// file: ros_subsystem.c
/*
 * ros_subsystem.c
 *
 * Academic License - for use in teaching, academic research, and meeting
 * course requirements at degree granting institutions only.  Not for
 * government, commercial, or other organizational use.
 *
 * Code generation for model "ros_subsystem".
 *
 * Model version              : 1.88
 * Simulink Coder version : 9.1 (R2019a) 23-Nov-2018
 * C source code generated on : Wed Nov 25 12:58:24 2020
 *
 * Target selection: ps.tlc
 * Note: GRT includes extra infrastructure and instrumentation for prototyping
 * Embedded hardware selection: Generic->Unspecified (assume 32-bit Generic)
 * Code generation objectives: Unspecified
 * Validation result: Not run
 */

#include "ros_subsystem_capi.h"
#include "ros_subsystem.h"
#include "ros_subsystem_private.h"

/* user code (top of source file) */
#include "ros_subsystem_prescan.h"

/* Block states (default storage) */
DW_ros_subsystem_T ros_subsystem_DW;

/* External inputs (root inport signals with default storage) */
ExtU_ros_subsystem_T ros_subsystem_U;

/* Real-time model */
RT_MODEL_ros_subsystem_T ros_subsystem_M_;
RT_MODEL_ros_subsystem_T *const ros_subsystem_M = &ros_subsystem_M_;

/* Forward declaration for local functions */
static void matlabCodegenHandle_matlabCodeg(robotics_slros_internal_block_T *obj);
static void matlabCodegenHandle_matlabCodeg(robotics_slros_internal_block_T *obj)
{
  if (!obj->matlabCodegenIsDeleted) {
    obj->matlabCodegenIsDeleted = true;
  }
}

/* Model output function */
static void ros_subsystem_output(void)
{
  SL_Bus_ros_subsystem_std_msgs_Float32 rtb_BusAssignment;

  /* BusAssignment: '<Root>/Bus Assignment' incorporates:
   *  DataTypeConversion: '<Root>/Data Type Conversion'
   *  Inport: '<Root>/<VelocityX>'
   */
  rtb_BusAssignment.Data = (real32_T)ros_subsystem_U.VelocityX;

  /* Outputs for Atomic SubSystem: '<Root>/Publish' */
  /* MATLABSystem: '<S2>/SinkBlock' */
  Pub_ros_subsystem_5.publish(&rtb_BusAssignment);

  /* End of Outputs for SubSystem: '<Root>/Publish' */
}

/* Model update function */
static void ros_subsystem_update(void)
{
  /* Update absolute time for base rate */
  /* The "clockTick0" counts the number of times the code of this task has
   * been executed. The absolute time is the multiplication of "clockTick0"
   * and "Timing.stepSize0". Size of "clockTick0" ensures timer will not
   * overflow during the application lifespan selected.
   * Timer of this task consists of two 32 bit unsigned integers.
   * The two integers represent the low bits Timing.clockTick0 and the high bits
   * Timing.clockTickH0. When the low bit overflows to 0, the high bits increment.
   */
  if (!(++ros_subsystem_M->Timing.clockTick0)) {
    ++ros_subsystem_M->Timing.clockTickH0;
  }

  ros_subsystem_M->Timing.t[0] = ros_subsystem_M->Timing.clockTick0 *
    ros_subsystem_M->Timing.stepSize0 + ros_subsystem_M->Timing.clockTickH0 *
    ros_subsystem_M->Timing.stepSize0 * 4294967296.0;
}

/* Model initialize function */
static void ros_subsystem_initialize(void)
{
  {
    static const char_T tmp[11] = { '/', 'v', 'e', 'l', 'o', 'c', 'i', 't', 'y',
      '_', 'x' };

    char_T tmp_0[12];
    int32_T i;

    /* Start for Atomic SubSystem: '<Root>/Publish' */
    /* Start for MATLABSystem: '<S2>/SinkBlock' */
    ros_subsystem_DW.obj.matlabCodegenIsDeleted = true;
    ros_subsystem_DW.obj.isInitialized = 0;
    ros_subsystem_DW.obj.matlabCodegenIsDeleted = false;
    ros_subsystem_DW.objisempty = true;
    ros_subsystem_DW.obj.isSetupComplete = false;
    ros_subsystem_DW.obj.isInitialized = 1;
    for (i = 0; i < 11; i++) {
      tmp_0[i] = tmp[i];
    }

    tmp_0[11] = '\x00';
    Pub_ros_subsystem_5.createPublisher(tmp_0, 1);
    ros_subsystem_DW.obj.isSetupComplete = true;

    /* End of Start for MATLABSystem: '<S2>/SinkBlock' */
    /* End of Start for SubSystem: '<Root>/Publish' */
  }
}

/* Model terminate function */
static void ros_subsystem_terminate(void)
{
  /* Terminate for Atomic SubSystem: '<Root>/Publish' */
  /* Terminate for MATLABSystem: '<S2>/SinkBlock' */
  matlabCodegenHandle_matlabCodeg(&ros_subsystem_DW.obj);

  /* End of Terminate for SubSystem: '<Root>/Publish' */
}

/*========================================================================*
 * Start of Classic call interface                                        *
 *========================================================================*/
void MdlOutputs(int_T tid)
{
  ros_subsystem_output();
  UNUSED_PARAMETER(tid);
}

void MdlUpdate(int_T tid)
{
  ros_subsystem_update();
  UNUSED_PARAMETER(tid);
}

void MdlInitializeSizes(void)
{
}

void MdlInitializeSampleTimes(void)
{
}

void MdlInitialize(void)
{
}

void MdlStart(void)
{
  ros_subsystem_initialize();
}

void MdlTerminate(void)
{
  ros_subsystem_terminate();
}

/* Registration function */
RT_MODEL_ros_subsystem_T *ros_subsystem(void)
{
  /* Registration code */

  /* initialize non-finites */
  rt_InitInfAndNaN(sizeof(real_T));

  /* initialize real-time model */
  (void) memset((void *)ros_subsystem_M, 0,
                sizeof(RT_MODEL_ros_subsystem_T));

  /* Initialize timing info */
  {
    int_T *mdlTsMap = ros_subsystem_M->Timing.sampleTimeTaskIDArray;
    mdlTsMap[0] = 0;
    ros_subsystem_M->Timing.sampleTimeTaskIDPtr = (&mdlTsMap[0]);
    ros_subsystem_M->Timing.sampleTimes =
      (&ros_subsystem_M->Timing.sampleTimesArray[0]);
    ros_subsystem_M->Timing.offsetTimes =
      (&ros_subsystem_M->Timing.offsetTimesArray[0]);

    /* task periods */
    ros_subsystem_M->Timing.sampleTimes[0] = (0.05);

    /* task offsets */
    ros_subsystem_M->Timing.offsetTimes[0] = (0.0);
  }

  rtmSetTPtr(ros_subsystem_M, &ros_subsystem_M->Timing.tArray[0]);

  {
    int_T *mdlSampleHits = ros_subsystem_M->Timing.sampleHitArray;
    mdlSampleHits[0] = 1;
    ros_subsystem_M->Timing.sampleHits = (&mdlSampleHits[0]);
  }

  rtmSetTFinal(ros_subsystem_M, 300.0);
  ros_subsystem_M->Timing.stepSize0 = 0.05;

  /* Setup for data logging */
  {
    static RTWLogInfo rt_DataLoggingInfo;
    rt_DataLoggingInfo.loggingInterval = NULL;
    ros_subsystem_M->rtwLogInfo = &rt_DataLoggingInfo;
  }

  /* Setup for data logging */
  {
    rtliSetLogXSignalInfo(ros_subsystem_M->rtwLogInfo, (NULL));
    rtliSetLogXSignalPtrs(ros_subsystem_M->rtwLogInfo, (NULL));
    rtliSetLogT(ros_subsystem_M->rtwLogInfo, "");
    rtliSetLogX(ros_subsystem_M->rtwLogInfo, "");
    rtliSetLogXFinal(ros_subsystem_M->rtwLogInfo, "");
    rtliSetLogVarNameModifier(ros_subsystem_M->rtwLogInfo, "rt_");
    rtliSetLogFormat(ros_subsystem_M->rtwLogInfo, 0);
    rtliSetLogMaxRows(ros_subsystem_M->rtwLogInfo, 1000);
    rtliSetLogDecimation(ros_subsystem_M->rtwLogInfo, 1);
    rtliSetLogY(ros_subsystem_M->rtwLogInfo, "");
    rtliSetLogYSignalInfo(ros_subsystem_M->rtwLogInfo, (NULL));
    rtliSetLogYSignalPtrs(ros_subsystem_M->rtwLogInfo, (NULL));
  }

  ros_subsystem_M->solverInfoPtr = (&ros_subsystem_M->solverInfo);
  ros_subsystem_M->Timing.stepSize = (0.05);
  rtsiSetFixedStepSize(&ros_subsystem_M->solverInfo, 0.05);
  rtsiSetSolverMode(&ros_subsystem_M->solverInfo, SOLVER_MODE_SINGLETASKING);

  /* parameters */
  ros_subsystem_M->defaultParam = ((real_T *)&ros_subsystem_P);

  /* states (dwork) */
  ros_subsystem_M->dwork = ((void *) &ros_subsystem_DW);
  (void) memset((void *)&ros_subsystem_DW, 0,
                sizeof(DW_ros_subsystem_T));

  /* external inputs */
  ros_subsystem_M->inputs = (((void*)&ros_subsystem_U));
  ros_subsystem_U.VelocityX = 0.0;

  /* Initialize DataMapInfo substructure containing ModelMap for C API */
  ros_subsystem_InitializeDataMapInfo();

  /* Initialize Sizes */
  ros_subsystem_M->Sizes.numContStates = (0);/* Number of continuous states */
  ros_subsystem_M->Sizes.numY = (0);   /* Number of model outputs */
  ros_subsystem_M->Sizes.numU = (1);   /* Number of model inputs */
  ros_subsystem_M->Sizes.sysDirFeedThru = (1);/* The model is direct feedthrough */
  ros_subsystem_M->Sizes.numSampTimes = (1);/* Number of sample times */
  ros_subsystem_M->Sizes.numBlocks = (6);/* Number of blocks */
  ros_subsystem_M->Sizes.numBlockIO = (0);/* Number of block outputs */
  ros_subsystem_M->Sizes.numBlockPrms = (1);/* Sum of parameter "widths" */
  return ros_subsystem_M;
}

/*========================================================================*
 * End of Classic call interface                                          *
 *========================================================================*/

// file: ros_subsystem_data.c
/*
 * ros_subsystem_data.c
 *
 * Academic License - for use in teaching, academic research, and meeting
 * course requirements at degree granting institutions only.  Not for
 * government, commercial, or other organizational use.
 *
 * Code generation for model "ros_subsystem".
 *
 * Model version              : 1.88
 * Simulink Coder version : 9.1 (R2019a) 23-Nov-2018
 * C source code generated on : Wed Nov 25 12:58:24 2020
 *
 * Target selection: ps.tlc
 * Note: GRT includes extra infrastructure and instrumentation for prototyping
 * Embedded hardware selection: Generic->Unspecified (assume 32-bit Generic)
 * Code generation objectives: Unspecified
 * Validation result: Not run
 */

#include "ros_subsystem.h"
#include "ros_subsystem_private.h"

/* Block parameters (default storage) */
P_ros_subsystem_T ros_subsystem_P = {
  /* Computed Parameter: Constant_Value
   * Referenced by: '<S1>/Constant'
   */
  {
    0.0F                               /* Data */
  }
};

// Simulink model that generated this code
simulink model "ros_subsystem"  (R2019a)
settings: Solver=ode5  StartTime=0.0  StopTime=300  FixedStep=0.05  RelTol=1e-3
model workspace (MAT data in the model file):
  mbox_table : struct (value not decoded)
  model_closed = 0
  sim_status = 0
libraries: robotlib x2

== system ros_subsystem ==
  <VelocityX> : Inport  OutDataTypeStr=double  PortDimensions=1  SampleTime=[0.050000000000000003,0]
  Blank Message : robotlib/Blank Message  messageClass=Message  entityType=std_msgs/Float32  messageType=std_msgs/Float32  SampleTime=inf
  Bus Assignment : BusAssignment  AssignedSignals=Data
  Data Type Conversion : DataTypeConversion  OutDataTypeStr=single
  Publish : robotlib/Publish  topicSource=Specify your own  topic=/velocity_x  messageType=std_msgs/Float32  messageQueueLength=1
  wires:
  Bus Assignment/1 -> Publish/1
  Blank Message/1 -> Bus Assignment/1
  <VelocityX>/1 -> Data Type Conversion/1  "VelocityX"
  Data Type Conversion/1 -> Bus Assignment/2
